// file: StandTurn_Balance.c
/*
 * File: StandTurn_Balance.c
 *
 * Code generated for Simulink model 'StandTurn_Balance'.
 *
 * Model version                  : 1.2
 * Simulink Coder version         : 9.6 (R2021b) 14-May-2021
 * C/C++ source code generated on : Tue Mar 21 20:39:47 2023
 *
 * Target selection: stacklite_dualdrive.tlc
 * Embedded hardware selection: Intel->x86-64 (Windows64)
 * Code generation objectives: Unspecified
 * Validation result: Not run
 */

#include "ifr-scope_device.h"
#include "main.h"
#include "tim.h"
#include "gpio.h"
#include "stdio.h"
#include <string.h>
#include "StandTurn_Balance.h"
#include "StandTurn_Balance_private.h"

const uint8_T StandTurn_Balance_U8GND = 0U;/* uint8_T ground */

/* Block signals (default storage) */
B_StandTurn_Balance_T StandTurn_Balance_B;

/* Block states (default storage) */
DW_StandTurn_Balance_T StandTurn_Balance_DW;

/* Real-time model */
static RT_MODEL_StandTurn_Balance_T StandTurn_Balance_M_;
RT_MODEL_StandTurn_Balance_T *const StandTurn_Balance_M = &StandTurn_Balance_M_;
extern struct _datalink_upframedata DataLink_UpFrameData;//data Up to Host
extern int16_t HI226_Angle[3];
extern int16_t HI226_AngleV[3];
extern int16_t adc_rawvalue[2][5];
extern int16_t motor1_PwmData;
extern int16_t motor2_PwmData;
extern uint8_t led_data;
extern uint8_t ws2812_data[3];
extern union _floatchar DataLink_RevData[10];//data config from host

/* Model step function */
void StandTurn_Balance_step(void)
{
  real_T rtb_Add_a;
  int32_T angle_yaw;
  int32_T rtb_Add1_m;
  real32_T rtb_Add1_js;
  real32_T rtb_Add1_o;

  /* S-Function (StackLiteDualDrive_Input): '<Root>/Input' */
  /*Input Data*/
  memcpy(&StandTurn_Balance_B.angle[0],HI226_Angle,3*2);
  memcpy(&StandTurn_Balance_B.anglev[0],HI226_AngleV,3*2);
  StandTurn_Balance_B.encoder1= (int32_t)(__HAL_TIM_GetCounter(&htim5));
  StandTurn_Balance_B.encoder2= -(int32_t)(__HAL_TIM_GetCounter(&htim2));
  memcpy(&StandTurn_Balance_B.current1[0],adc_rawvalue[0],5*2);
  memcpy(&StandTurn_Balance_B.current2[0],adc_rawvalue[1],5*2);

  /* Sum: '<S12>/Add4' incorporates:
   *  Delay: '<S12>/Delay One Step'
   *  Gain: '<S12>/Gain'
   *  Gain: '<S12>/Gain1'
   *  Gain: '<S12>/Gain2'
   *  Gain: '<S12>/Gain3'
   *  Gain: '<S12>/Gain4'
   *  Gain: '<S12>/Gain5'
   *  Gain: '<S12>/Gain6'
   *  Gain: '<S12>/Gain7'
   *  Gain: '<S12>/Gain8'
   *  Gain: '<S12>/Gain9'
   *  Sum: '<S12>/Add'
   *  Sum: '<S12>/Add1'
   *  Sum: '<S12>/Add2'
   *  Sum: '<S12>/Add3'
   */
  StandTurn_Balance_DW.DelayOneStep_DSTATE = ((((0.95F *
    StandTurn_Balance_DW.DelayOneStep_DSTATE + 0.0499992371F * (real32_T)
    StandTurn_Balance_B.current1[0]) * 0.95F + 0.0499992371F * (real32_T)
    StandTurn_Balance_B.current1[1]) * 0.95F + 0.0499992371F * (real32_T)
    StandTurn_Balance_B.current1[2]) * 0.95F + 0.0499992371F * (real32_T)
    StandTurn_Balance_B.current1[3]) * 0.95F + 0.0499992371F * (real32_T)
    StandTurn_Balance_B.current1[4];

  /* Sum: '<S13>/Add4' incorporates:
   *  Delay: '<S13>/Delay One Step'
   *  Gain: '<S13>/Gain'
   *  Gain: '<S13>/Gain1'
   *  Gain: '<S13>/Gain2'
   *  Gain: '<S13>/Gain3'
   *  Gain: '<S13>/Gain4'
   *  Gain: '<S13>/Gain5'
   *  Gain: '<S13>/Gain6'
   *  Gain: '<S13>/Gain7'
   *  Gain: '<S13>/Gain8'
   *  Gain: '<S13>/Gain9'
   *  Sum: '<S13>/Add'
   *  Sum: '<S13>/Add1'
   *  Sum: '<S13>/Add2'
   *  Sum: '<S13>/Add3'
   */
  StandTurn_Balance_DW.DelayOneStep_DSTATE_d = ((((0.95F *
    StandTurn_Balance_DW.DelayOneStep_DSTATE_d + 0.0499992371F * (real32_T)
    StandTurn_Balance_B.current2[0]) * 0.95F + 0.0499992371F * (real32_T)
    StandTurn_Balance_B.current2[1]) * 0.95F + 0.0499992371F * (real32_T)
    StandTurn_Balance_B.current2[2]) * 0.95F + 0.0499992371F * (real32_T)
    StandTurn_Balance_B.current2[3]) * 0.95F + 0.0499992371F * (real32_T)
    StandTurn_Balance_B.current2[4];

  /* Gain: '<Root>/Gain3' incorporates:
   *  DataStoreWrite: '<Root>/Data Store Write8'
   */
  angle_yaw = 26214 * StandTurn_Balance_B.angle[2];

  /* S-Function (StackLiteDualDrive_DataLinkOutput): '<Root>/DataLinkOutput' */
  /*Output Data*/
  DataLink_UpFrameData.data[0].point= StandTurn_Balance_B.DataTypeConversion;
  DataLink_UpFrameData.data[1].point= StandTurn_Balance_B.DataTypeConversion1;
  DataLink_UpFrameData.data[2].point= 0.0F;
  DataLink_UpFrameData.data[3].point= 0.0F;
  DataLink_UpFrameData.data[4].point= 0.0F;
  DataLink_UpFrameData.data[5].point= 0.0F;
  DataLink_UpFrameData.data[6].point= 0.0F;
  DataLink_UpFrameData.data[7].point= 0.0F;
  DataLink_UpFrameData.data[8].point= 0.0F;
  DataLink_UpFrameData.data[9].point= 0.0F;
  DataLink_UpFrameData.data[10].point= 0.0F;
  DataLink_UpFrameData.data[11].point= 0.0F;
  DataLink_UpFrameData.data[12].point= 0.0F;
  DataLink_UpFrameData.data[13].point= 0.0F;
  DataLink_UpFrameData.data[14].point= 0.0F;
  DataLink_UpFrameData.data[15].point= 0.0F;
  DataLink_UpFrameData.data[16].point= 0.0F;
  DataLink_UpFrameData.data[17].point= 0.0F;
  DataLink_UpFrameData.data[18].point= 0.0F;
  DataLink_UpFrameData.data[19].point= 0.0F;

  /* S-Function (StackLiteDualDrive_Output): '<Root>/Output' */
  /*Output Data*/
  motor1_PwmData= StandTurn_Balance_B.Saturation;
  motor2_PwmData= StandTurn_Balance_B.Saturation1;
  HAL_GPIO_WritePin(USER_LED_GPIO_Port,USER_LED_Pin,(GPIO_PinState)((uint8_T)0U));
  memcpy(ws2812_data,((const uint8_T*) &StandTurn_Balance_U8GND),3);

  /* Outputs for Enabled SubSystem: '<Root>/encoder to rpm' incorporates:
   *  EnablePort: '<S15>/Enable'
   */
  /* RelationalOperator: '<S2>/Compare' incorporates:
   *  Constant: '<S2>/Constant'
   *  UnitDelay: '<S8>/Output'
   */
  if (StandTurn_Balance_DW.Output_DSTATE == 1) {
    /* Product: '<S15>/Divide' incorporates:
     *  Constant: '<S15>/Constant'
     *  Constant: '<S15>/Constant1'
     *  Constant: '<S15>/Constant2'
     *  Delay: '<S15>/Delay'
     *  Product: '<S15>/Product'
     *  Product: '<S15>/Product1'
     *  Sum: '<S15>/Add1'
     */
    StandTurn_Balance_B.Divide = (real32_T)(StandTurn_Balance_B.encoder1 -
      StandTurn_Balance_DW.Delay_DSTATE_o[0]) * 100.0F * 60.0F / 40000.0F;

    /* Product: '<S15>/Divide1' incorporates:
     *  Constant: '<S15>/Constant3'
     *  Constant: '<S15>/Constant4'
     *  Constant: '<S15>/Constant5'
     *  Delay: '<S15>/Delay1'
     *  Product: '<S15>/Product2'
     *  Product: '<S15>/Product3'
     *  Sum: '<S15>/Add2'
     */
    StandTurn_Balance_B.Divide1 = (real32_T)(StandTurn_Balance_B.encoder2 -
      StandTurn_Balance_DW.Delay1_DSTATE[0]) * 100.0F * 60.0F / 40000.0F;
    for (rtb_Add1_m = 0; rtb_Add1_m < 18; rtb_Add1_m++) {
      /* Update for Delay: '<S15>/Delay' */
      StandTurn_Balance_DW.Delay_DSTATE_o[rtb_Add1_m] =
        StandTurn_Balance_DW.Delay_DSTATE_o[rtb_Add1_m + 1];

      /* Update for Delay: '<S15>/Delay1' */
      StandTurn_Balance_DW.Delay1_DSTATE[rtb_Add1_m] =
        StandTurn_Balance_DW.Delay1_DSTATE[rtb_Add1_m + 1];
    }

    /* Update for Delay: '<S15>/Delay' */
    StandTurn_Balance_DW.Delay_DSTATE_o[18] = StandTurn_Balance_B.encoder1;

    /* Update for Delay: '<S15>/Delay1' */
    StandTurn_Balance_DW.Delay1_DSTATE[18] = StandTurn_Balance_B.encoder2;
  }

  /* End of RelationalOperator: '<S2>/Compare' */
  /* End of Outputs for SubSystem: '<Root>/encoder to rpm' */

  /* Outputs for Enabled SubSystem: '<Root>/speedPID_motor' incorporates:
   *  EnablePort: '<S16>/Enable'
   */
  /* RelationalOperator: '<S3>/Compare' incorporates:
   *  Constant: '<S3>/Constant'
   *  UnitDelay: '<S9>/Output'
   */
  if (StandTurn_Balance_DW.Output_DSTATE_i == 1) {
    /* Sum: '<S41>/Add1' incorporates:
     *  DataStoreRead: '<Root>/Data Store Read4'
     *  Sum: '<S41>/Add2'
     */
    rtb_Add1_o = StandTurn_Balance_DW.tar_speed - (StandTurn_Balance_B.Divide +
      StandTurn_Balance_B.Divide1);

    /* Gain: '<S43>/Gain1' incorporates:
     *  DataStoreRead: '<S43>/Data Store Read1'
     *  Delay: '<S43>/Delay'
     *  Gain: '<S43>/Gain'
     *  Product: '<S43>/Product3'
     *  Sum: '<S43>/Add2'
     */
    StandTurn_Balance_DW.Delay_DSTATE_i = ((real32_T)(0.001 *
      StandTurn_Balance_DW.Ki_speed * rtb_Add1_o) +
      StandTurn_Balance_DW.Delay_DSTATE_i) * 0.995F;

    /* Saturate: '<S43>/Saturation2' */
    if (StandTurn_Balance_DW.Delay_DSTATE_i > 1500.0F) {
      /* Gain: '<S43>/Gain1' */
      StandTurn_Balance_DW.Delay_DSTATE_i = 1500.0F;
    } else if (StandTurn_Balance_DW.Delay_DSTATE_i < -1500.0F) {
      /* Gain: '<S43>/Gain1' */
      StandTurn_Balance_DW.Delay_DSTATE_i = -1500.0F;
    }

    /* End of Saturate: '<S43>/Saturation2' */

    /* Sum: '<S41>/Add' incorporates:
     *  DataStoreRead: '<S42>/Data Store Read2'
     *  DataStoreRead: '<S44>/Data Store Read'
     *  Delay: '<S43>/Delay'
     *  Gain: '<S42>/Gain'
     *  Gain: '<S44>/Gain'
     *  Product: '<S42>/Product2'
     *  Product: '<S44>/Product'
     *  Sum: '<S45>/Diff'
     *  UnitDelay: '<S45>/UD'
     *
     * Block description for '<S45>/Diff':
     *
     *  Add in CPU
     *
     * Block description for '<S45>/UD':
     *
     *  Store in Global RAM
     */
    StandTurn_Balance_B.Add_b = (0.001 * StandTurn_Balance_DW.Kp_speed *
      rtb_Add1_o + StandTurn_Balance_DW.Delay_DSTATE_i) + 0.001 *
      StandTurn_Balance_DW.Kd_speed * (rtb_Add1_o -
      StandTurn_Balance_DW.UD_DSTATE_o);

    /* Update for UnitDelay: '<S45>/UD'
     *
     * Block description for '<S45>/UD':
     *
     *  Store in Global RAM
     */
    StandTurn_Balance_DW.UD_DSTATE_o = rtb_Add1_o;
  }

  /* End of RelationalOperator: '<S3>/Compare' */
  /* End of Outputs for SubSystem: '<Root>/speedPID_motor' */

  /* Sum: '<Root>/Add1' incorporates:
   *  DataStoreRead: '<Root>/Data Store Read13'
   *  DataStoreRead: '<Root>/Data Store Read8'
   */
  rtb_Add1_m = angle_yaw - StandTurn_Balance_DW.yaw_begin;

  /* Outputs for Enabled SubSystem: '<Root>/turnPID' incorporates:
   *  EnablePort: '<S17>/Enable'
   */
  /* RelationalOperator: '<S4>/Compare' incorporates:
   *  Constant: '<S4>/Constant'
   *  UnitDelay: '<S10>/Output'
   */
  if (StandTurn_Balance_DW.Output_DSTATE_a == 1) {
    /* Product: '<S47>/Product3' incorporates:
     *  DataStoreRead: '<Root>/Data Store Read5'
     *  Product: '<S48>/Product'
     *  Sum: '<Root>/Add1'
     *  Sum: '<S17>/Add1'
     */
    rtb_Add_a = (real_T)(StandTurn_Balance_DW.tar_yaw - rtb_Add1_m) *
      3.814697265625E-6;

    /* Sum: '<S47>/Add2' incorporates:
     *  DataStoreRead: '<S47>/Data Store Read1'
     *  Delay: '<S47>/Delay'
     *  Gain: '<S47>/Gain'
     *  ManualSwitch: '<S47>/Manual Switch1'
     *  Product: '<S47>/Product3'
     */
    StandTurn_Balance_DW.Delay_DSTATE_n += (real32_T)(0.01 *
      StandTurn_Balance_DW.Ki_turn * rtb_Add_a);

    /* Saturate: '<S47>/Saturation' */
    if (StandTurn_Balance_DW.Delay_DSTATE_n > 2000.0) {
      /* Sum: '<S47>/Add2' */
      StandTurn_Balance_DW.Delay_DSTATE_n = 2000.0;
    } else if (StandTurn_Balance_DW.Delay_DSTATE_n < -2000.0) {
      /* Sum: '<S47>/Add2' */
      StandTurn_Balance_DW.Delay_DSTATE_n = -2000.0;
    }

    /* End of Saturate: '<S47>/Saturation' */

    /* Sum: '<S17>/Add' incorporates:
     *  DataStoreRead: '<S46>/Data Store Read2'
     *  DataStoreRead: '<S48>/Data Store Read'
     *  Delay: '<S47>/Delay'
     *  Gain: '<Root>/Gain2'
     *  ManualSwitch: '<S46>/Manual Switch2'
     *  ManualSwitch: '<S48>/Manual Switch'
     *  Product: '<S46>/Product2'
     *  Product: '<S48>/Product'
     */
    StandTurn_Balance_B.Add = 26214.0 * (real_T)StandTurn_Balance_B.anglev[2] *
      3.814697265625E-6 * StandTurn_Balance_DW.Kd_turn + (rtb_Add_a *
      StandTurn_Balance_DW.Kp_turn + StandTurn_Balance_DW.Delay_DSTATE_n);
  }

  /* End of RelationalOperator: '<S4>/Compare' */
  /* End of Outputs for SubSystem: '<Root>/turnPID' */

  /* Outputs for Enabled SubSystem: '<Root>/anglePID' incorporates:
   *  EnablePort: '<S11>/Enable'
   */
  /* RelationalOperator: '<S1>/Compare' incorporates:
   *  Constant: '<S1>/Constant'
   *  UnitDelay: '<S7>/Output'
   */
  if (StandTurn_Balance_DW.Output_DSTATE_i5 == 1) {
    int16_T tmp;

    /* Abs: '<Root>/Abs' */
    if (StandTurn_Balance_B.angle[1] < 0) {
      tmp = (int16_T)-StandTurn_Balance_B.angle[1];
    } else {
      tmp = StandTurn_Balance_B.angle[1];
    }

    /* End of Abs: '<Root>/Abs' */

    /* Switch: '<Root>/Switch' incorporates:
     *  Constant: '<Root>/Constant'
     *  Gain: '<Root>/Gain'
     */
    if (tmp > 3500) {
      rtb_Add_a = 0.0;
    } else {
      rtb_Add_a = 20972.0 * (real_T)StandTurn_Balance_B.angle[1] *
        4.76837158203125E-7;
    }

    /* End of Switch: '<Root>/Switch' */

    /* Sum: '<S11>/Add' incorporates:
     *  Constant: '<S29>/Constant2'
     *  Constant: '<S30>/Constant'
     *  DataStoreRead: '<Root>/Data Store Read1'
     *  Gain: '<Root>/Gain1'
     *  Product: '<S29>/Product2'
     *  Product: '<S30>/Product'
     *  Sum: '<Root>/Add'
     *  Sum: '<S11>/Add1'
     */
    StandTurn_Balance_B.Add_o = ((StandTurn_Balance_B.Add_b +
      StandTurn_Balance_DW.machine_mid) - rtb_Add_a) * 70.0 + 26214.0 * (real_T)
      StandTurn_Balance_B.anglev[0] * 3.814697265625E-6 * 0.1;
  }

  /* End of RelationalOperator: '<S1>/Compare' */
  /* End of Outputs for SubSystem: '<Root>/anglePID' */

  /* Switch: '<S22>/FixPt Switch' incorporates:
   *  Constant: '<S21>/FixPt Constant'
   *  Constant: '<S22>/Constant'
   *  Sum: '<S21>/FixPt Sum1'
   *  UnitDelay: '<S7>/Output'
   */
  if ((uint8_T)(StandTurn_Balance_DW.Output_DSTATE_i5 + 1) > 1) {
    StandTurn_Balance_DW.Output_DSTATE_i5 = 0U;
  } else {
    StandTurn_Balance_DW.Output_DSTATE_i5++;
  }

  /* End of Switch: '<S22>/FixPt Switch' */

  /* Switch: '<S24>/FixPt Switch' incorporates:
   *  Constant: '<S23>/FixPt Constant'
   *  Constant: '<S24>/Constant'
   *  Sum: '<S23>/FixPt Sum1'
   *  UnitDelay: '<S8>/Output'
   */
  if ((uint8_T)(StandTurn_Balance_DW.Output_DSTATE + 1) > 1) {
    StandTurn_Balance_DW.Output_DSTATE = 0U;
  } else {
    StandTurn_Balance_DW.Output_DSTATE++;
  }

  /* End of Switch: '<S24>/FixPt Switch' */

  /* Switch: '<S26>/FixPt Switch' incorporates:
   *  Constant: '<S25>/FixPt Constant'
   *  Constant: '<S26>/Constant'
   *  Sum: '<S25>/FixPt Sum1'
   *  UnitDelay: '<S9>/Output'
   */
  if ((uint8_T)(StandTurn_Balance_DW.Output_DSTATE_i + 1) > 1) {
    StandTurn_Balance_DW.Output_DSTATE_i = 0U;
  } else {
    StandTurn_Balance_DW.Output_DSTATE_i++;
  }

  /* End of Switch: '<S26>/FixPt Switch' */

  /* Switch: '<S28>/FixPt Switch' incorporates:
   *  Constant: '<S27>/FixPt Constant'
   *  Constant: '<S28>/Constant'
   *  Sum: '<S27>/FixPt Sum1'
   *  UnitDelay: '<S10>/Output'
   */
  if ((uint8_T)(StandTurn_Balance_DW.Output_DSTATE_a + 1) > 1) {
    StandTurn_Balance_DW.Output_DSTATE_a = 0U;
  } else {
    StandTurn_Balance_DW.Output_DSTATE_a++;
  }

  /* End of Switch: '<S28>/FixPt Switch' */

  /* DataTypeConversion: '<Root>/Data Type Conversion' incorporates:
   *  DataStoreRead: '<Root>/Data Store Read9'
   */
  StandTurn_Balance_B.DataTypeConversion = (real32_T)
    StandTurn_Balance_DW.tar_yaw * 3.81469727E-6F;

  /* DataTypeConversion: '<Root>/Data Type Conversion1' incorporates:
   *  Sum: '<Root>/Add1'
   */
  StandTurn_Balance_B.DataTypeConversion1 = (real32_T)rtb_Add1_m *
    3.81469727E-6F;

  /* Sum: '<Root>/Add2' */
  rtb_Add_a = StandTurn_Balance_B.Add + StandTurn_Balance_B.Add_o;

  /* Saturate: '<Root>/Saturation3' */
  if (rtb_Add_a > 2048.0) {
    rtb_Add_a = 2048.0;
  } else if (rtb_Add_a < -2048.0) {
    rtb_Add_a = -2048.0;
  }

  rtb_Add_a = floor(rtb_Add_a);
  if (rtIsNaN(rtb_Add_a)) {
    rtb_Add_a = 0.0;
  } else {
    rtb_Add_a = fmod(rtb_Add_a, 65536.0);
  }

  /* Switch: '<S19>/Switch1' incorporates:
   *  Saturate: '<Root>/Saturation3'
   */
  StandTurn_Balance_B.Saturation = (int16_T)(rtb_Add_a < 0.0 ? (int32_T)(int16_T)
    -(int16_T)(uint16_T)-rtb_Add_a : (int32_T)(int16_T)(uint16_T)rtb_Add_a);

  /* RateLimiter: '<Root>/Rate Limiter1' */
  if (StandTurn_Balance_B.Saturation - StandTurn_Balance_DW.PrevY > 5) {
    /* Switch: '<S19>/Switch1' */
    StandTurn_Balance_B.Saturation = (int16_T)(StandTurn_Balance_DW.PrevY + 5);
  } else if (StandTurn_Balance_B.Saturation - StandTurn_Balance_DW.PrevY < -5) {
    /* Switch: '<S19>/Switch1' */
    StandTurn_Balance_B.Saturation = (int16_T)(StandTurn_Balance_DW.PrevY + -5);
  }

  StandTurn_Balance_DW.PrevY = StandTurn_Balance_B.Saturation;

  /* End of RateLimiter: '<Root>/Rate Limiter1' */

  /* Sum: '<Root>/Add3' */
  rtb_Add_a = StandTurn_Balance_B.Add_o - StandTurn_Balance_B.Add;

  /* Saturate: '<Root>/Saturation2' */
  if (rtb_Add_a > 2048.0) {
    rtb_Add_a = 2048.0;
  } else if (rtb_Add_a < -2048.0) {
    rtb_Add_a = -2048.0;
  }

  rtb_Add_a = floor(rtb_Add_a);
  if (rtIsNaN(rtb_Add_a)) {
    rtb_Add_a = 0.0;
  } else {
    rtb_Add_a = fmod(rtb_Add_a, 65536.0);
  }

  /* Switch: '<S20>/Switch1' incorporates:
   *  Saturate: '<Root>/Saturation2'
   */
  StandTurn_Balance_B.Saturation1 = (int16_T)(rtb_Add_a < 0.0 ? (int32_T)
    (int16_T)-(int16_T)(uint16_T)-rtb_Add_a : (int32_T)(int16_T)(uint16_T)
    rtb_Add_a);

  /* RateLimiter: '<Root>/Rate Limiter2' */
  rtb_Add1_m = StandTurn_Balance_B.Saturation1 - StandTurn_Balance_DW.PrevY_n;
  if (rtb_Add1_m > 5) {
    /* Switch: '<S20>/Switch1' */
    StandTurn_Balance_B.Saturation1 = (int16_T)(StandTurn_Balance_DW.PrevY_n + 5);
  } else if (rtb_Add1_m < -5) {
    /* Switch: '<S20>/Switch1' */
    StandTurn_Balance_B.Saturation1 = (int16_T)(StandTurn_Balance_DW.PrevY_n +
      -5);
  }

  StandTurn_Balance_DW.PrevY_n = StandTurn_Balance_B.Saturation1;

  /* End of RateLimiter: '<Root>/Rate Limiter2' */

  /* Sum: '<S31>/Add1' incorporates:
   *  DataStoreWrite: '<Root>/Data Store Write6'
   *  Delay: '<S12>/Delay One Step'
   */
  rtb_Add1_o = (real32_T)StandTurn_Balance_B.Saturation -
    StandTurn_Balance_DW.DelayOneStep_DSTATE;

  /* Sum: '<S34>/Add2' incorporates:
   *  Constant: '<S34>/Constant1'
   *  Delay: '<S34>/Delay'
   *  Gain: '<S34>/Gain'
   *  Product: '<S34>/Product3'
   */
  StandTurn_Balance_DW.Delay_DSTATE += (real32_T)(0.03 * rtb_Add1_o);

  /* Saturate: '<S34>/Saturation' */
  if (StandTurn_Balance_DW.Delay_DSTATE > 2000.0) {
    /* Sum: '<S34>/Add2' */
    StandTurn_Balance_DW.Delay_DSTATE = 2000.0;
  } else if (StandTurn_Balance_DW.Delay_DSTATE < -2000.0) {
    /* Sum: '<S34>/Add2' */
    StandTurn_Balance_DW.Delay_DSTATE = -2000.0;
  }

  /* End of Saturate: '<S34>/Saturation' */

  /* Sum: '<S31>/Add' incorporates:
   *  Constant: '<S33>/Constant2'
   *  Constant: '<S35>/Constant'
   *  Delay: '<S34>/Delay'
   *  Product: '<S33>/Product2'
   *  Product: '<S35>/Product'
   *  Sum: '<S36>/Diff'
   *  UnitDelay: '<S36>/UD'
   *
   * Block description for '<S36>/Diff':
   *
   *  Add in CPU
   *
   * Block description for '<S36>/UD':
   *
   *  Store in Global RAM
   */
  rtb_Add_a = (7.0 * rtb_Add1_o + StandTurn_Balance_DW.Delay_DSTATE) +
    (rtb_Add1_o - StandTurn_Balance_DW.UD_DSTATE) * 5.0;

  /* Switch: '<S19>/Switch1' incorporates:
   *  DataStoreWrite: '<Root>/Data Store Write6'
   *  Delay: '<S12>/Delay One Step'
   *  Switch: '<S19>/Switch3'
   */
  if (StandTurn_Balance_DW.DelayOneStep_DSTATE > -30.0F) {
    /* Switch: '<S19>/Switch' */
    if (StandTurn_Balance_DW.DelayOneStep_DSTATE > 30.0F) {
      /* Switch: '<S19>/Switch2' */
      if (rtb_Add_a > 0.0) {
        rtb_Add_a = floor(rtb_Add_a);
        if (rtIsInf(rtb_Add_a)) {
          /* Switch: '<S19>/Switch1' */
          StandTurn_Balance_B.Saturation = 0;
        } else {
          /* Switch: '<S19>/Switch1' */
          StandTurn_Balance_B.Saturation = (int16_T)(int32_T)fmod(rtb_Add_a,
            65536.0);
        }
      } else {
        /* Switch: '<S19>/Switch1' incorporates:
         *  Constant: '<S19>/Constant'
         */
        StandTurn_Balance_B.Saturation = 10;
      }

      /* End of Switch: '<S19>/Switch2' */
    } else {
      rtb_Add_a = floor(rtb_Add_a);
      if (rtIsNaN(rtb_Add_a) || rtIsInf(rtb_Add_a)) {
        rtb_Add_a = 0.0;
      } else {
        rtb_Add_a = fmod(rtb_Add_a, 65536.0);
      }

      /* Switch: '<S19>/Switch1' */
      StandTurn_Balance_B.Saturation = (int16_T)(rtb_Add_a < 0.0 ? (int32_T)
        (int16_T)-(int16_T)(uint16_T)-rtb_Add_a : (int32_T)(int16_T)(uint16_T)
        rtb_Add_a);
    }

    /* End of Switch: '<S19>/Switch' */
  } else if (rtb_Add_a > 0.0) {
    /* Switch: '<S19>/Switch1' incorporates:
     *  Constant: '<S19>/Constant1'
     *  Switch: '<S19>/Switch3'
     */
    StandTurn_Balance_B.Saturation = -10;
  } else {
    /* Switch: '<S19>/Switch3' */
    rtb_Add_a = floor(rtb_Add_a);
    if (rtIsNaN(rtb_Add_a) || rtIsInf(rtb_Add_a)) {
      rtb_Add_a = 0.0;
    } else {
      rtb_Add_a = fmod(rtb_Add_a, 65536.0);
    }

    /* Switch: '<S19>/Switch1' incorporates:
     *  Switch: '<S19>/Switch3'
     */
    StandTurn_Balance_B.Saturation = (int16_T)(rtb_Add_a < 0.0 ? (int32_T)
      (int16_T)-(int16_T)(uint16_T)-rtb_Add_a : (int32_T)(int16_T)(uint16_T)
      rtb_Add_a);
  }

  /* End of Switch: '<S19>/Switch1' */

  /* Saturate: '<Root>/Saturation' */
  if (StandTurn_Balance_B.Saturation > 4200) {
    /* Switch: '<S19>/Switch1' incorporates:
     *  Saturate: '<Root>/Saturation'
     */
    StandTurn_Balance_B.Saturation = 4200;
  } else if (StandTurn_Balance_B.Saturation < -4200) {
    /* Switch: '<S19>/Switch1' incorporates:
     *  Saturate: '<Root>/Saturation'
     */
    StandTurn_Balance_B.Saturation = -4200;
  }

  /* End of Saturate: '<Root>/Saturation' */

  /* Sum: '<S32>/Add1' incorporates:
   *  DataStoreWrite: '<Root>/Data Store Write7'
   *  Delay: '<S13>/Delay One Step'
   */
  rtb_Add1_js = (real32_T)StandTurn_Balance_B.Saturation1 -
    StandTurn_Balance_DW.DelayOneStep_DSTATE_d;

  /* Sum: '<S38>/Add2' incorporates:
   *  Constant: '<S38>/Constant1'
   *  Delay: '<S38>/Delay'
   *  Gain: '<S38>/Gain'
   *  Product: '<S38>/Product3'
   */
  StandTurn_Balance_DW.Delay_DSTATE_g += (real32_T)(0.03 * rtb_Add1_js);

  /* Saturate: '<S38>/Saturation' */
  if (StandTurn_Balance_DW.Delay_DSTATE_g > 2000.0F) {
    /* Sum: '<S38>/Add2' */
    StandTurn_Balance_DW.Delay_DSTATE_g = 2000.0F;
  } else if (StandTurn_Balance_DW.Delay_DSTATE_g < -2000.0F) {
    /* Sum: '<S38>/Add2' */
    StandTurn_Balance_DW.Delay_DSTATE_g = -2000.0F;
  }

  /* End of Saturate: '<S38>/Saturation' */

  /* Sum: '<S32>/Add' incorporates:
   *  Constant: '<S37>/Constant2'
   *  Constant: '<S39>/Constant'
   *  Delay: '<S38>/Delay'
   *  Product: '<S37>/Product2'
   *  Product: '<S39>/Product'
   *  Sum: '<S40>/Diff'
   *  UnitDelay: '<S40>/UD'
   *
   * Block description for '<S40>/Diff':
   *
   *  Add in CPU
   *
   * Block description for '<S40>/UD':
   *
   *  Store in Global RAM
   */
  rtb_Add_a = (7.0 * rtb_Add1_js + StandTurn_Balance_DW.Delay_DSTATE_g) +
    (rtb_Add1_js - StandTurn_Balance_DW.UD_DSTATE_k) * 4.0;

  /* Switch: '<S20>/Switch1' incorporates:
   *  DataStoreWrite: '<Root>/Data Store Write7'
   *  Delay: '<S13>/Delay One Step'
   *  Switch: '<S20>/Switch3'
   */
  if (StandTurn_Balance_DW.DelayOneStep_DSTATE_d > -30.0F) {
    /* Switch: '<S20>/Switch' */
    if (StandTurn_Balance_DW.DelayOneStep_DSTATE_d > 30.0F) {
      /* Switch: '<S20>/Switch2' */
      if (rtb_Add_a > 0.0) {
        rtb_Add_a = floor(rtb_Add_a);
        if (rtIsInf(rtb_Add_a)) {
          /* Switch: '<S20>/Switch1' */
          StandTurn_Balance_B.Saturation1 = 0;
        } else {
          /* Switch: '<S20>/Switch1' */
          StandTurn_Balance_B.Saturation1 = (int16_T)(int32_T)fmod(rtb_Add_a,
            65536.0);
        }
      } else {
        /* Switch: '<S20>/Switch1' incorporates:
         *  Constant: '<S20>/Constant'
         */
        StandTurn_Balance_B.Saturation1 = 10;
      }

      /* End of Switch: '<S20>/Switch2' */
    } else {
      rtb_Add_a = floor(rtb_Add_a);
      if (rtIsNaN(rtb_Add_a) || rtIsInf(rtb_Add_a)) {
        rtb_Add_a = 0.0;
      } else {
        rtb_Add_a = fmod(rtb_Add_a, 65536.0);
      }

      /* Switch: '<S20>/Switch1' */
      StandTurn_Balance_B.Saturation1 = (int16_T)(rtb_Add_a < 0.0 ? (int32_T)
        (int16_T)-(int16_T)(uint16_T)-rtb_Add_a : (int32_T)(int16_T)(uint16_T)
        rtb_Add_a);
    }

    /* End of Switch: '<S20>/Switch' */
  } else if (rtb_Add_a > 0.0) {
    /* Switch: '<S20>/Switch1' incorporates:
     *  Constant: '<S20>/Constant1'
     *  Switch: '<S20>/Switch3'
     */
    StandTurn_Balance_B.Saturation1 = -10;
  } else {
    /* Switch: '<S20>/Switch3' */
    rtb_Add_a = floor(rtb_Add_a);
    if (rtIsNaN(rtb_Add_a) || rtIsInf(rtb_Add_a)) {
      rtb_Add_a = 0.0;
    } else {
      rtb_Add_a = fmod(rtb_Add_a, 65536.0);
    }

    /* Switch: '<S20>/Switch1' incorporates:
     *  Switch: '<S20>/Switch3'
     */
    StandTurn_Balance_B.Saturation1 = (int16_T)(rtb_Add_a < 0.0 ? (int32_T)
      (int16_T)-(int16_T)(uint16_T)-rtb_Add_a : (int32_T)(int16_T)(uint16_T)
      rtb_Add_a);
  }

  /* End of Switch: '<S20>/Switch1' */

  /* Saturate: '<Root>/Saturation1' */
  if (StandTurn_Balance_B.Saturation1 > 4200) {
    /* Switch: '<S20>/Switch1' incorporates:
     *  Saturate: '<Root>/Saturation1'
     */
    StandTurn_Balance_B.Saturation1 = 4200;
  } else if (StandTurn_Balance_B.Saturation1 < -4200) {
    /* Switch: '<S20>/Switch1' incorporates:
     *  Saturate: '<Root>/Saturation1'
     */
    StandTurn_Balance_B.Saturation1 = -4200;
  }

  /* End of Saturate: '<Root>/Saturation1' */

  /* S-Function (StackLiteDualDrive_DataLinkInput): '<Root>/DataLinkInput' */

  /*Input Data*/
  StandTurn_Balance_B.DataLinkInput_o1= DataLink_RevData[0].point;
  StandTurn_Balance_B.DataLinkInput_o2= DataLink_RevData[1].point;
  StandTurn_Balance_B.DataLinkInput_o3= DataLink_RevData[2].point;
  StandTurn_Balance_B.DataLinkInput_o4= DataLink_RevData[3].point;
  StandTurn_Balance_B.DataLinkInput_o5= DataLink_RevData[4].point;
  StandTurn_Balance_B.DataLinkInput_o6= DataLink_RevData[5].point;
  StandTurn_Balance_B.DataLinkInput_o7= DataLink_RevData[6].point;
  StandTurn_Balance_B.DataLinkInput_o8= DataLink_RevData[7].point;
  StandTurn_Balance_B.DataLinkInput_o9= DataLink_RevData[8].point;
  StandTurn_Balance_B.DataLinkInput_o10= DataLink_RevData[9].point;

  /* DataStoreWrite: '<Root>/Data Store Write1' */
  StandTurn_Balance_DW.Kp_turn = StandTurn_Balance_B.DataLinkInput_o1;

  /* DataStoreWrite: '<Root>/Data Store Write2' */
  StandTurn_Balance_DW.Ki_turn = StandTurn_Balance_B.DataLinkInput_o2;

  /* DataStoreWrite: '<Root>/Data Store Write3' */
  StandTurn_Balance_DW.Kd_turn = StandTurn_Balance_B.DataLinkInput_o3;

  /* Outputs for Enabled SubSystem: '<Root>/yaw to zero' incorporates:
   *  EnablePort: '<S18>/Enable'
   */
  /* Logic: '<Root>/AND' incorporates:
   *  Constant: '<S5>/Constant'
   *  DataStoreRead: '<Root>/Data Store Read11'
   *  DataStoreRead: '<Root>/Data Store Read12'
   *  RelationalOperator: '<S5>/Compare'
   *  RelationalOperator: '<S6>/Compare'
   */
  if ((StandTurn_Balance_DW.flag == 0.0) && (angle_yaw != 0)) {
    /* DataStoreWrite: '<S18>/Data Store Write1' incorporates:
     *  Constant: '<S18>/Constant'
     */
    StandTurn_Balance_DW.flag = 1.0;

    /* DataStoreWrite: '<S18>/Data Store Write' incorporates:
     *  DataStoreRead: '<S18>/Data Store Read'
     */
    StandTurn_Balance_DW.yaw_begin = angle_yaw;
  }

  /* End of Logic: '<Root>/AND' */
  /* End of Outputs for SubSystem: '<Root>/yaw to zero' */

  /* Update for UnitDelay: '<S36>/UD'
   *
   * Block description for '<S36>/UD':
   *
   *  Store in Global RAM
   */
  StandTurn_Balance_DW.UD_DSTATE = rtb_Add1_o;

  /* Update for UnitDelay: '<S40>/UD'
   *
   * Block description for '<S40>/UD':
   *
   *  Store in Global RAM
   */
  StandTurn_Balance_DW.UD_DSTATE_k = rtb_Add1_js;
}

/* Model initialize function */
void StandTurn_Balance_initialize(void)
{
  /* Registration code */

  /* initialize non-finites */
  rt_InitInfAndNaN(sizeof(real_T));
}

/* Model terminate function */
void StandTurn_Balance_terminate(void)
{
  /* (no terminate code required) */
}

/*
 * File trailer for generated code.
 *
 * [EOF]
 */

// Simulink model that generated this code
simulink model "StandTurn_Balance"  (R2021b)
settings: Solver=FixedStepDiscrete  StartTime=0.0  StopTime=inf  FixedStep=0.0005  RelTol=1e-3
libraries: simulink x13, IFR_StackLiteDualDrive_SimulinkLib x4

== system StandTurn_Balance ==
  AND : Logic  IconShape=distinctive  AllPortsSameDT=off  OutDataTypeStr=boolean
  Abs : Abs
  Add : Sum
  Add1 : Sum  Inputs=+-
  Add2 : Sum
  Add3 : Sum  Inputs=-+
  Compare To Constant{,1..3} (4 alike) : simulink/Logic and Bit Operations/Compare To Constant  relop===  const=1  OutDataTypeStr=boolean
  Compare To Constant4 : simulink/Logic and Bit Operations/Compare To Constant  relop===  const=0  OutDataTypeStr=boolean
  Compare To Constant5 : simulink/Logic and Bit Operations/Compare To Constant  relop=~=  const=0  OutDataTypeStr=boolean
  Constant : Constant  Value=0
  Counter Limited{,1..3} (4 alike) : simulink/Sources/Counter Limited  uplimit=1  tsamp=-1
  Data Store Memory : DataStoreMemory  DataStoreName=Kp_angle  ReadBeforeWriteMsg=warning  WriteAfterWriteMsg=warning  WriteAfterReadMsg=warning  ShowAdditionalParam=off
  Data Store Memory1 : DataStoreMemory  DataStoreName=angleV_pitch  ReadBeforeWriteMsg=warning  WriteAfterWriteMsg=warning  WriteAfterReadMsg=warning  ShowAdditionalParam=off
  Data Store Memory10 : DataStoreMemory  DataStoreName=flag  ReadBeforeWriteMsg=warning  WriteAfterWriteMsg=warning  WriteAfterReadMsg=warning  ShowAdditionalParam=off
  Data Store Memory11 : DataStoreMemory  DataStoreName=yaw_begin  ReadBeforeWriteMsg=warning  WriteAfterWriteMsg=warning  WriteAfterReadMsg=warning  ShowAdditionalParam=off
  Data Store Memory12 : DataStoreMemory  DataStoreName=tar_speed  ReadBeforeWriteMsg=warning  WriteAfterWriteMsg=warning  WriteAfterReadMsg=warning  ShowAdditionalParam=off
  Data Store Memory13 : DataStoreMemory  DataStoreName=Kp_speed  ReadBeforeWriteMsg=warning  WriteAfterWriteMsg=warning  WriteAfterReadMsg=warning  ShowAdditionalParam=off
  Data Store Memory14 : DataStoreMemory  DataStoreName=Ki_speed  ReadBeforeWriteMsg=warning  WriteAfterWriteMsg=warning  WriteAfterReadMsg=warning  ShowAdditionalParam=off
  Data Store Memory15 : DataStoreMemory  DataStoreName=Kd_speed  ReadBeforeWriteMsg=warning  WriteAfterWriteMsg=warning  WriteAfterReadMsg=warning  ShowAdditionalParam=off
  Data Store Memory16 : DataStoreMemory  DataStoreName=angleV_yaw  ReadBeforeWriteMsg=warning  WriteAfterWriteMsg=warning  WriteAfterReadMsg=warning  ShowAdditionalParam=off
  Data Store Memory19 : DataStoreMemory  DataStoreName=Kp_turn  ReadBeforeWriteMsg=warning  WriteAfterWriteMsg=warning  WriteAfterReadMsg=warning  ShowAdditionalParam=off
  Data Store Memory2 : DataStoreMemory  DataStoreName=Kd_angle  ReadBeforeWriteMsg=warning  WriteAfterWriteMsg=warning  WriteAfterReadMsg=warning  ShowAdditionalParam=off
  Data Store Memory20 : DataStoreMemory  DataStoreName=tar_yaw  ReadBeforeWriteMsg=warning  WriteAfterWriteMsg=warning  WriteAfterReadMsg=warning  ShowAdditionalParam=off
  Data Store Memory21 : DataStoreMemory  DataStoreName=angle_yaw  ReadBeforeWriteMsg=warning  WriteAfterWriteMsg=warning  WriteAfterReadMsg=warning  ShowAdditionalParam=off
  Data Store Memory22 : DataStoreMemory  DataStoreName=Ki_turn  ReadBeforeWriteMsg=warning  WriteAfterWriteMsg=warning  WriteAfterReadMsg=warning  ShowAdditionalParam=off
  Data Store Memory23 : DataStoreMemory  DataStoreName=Kd_turn  ReadBeforeWriteMsg=warning  WriteAfterWriteMsg=warning  WriteAfterReadMsg=warning  ShowAdditionalParam=off
  Data Store Memory3 : DataStoreMemory  DataStoreName=Kp_current  ReadBeforeWriteMsg=warning  WriteAfterWriteMsg=warning  WriteAfterReadMsg=warning  ShowAdditionalParam=off
  Data Store Memory4 : DataStoreMemory  DataStoreName=Ki_current  ReadBeforeWriteMsg=warning  WriteAfterWriteMsg=warning  WriteAfterReadMsg=warning  ShowAdditionalParam=off
  Data Store Memory5 : DataStoreMemory  DataStoreName=Kd_current  ReadBeforeWriteMsg=warning  WriteAfterWriteMsg=warning  WriteAfterReadMsg=warning  ShowAdditionalParam=off
  Data Store Memory6 : DataStoreMemory  DataStoreName=tar_current  ReadBeforeWriteMsg=warning  WriteAfterWriteMsg=warning  WriteAfterReadMsg=warning  ShowAdditionalParam=off
  Data Store Memory7 : DataStoreMemory  DataStoreName=machine_mid  ReadBeforeWriteMsg=warning  WriteAfterWriteMsg=warning  WriteAfterReadMsg=warning  ShowAdditionalParam=off
  Data Store Memory8 : DataStoreMemory  DataStoreName=now_current1  ReadBeforeWriteMsg=warning  WriteAfterWriteMsg=warning  WriteAfterReadMsg=warning  ShowAdditionalParam=off
  Data Store Memory9 : DataStoreMemory  DataStoreName=now_current2  ReadBeforeWriteMsg=warning  WriteAfterWriteMsg=warning  WriteAfterReadMsg=warning  ShowAdditionalParam=off
  Data Store Read : DataStoreRead  DataStoreName=tar_current  IndexOptions=Index vector (dialog)  Indices=1  OutputSizes=1
  Data Store Read1 : DataStoreRead  DataStoreName=machine_mid  IndexOptions=Index vector (dialog)  Indices=1  OutputSizes=1
  Data Store Read11 : DataStoreRead  DataStoreName=flag  IndexOptions=Index vector (dialog)  Indices=1  OutputSizes=1
  Data Store Read12 : DataStoreRead  DataStoreName=angle_yaw  IndexOptions=Index vector (dialog)  Indices=1  OutputSizes=1
  Data Store Read13 : DataStoreRead  DataStoreName=yaw_begin  IndexOptions=Index vector (dialog)  Indices=1  OutputSizes=1
  Data Store Read2 : DataStoreRead  DataStoreName=now_current1  IndexOptions=Index vector (dialog)  Indices=1  OutputSizes=1
  Data Store Read3 : DataStoreRead  DataStoreName=now_current2  IndexOptions=Index vector (dialog)  Indices=1  OutputSizes=1
  Data Store Read4 : DataStoreRead  DataStoreName=tar_speed  IndexOptions=Index vector (dialog)  Indices=1  OutputSizes=1
  Data Store Read5 : DataStoreRead  DataStoreName=tar_yaw  IndexOptions=Index vector (dialog)  Indices=1  OutputSizes=1
  Data Store Read6 : DataStoreRead  DataStoreName=now_current1  IndexOptions=Index vector (dialog)  Indices=1  OutputSizes=1
  Data Store Read7 : DataStoreRead  DataStoreName=now_current2  IndexOptions=Index vector (dialog)  Indices=1  OutputSizes=1
  Data Store Read8 : DataStoreRead  DataStoreName=angle_yaw  IndexOptions=Index vector (dialog)  Indices=1  OutputSizes=1
  Data Store Read9 : DataStoreRead  DataStoreName=tar_yaw  IndexOptions=Index vector (dialog)  Indices=1  OutputSizes=1
  Data Store Write : DataStoreWrite  DataStoreName=angleV_pitch  IndexOptions=Index vector (dialog)  Indices=1  OutputSizes=1
  Data Store Write1 : DataStoreWrite  DataStoreName=Kp_turn  IndexOptions=Index vector (dialog)  Indices=1  OutputSizes=1
  Data Store Write2 : DataStoreWrite  DataStoreName=Ki_turn  IndexOptions=Index vector (dialog)  Indices=1  OutputSizes=1
  Data Store Write3 : DataStoreWrite  DataStoreName=Kd_turn  IndexOptions=Index vector (dialog)  Indices=1  OutputSizes=1
  Data Store Write6 : DataStoreWrite  DataStoreName=now_current1  IndexOptions=Index vector (dialog)  Indices=1  OutputSizes=1
  Data Store Write7 : DataStoreWrite  DataStoreName=now_current2  IndexOptions=Index vector (dialog)  Indices=1  OutputSizes=1
  Data Store Write8 : DataStoreWrite  DataStoreName=angle_yaw  IndexOptions=Index vector (dialog)  Indices=1  OutputSizes=1
  Data Store Write9 : DataStoreWrite  DataStoreName=angleV_yaw  IndexOptions=Index vector (dialog)  Indices=1  OutputSizes=1
  Data Type Conversion : DataTypeConversion  OutDataTypeStr=single
  Data Type Conversion1 : DataTypeConversion  OutDataTypeStr=single
  DataLinkInput : IFR_StackLiteDualDrive_SimulinkLib/DataLinkInput
  DataLinkOutput : IFR_StackLiteDualDrive_SimulinkLib/DataLinkOutput  id='BalanceUnname'  key='IFR00'
  Demux : Demux  Outputs=3
  Demux1 : Demux  Outputs=5
  Demux2 : Demux  Outputs=5
  Demux3 : Demux  Outputs=3
  Gain : Gain  Gain=0.01
  Gain1 : Gain  Gain=0.1
  Gain2 : Gain  Gain=0.1
  Gain3 : Gain  Gain=0.1
  Input : IFR_StackLiteDualDrive_SimulinkLib/Input  Priority=0
  Manual Switch : ManualSwitch  CurrentSetting=0
  Output : IFR_StackLiteDualDrive_SimulinkLib/Output  Priority=255
  Rate Limiter1 : RateLimiter  RisingSlewLimit=10000  FallingSlewLimit=-10000  SampleTimeMode=inherited
  Rate Limiter2 : RateLimiter  RisingSlewLimit=10000  FallingSlewLimit=-10000  SampleTimeMode=inherited
  Saturation : Saturate  UpperLimit=4200  LowerLimit=-4200
  Saturation1 : Saturate  UpperLimit=4200  LowerLimit=-4200
  Saturation2 : Saturate  UpperLimit=2048  LowerLimit=-2048  OutDataTypeStr=int16
  Saturation3 : Saturate  UpperLimit=2048  LowerLimit=-2048  OutDataTypeStr=int16
  Switch : Switch  Criteria=u2 > Threshold  Threshold=3500
  Terminator{,1..8} (9 alike) : Terminator
  anglePID : Subsystem
  currentFilter_motor1 : Subsystem
  currentFilter_motor2 : Subsystem
  currentPID : Subsystem
  encoder to rpm : Subsystem
  speedPID_motor : Subsystem
  turnPID : Subsystem
  yaw to zero : Subsystem
  zero limit1 : Subsystem
  zero limit2 : Subsystem
  wires:
  Input/5 -> Demux2/1  "current1"
  Saturation1/1 -> Output/2
  Saturation2/1 -> Rate Limiter2/1
  Data Store Read3/1 -> currentPID/3(now_current2)
  Rate Limiter2/1 -> currentPID/4(tar_current2)
  Input/1 -> Demux/1  "angle"
  currentFilter_motor2/1(now_current) -> Data Store Write7/1
  Manual Switch/1 -> currentPID/1(tar_current1)
  Compare To Constant1/1 -> encoder to rpm/Enable
  Demux1/4 -> currentFilter_motor2/4(In4)
  Counter Limited1/1 -> Compare To Constant1/1
  Demux2/2 -> currentFilter_motor1/2(In2)
  zero limit2/1(pwmout) -> Saturation1/1  "motor2pwm"
  Demux1/1 -> currentFilter_motor2/1(In1)
  Demux2/5 -> currentFilter_motor1/5(In5)
  Input/3 -> encoder to rpm/1(encoder1)  "encoder1"
  Saturation3/1 -> Rate Limiter1/1
  Saturation/1 -> Output/1
  Demux1/3 -> currentFilter_motor2/3(In3)
  Input/6 -> Demux1/1  "current2"
  Demux2/3 -> currentFilter_motor1/3(In3)
  Demux/3 -> Gain3/1
  currentPID/2(tar_V2) -> zero limit2/1(pidout2pwm)
  Input/2 -> Demux3/1  "anglev"
  Demux3/2 -> Terminator6/1
  Demux2/1 -> currentFilter_motor1/1(In1)
  Demux1/5 -> currentFilter_motor2/5(In5)
  Input/4 -> encoder to rpm/2(encoder2)  "encoder2"
  currentPID/1(tar_V1) -> zero limit1/1(pidout1pwm)
  Demux1/2 -> currentFilter_motor2/2(In2)
  Data Store Read2/1 -> currentPID/2(now_current1)
  Data Store Read7/1 -> zero limit2/2(current2)
  currentFilter_motor1/1(now_current) -> Data Store Write6/1
  Rate Limiter1/1 -> Manual Switch/2
  Demux2/4 -> currentFilter_motor1/4(In4)
  zero limit1/1(pwmout) -> Saturation/1  "motor1pwm"
  Data Store Read/1 -> Manual Switch/1
  Data Store Read6/1 -> zero limit1/2(current1)
  Add/1 -> anglePID/1(tar_angle)
  Abs/1 -> Switch/2
  Gain/1 -> Switch/3
  Constant/1 -> Switch/1
  Demux/2 -> Gain/1, Abs/1
  Counter Limited/1 -> Compare To Constant/1
  Switch/1 -> anglePID/2(now_angle)
  Data Store Read1/1 -> Add/2
  Compare To Constant/1 -> anglePID/Enable
  Demux/1 -> Terminator7/1
  speedPID_motor/1(tar_sqangle) -> Add/1
  Demux3/1 -> Gain1/1
  Gain1/1 -> Data Store Write/1
  Data Store Read4/1 -> speedPID_motor/1(tar_speed)
  Counter Limited2/1 -> Compare To Constant2/1
  Compare To Constant2/1 -> speedPID_motor/Enable
  encoder to rpm/1(now_speed1) -> speedPID_motor/2(now_speed1)
  encoder to rpm/2(now_speed2) -> speedPID_motor/3(now_speed2)
  Data Store Read5/1 -> turnPID/1(tar_yaw)
  Demux3/3 -> Gain2/1
  Gain2/1 -> Data Store Write9/1
  Gain3/1 -> Data Store Write8/1
  turnPID/1(tar_I) -> Add3/1, Add2/1
  anglePID/1(tar_I) -> Add2/2, Add3/2
  Add2/1 -> Saturation3/1
  Add3/1 -> Saturation2/1
  Compare To Constant3/1 -> turnPID/Enable
  Counter Limited3/1 -> Compare To Constant3/1
  Data Store Read9/1 -> Data Type Conversion/1
  Data Type Conversion/1 -> DataLinkOutput/1
  Add1/1 -> Data Type Conversion1/1, turnPID/2(now_yaw)
  Data Type Conversion1/1 -> DataLinkOutput/2
  Data Store Read11/1 -> Compare To Constant4/1
  Data Store Read12/1 -> Compare To Constant5/1
  Compare To Constant4/1 -> AND/1
  Compare To Constant5/1 -> AND/2
  AND/1 -> yaw to zero/Enable
  Data Store Read8/1 -> Add1/1
  Data Store Read13/1 -> Add1/2
  DataLinkInput/10 -> Terminator/1
  DataLinkInput/9 -> Terminator1/1
  DataLinkInput/8 -> Terminator2/1
  DataLinkInput/7 -> Terminator3/1
  DataLinkInput/6 -> Terminator4/1
  DataLinkInput/5 -> Terminator5/1
  DataLinkInput/4 -> Terminator8/1
  DataLinkInput/1 -> Data Store Write1/1
  DataLinkInput/2 -> Data Store Write2/1
  DataLinkInput/3 -> Data Store Write3/1

== system StandTurn_Balance/anglePID ==
  tar_angle : Inport
  now_angle : Inport  Port=2
  Enable : EnablePort
  Add : Sum  OutDataTypeStr=double
  Add1 : Sum  Inputs=+-
  D : Subsystem
  P : Subsystem
  tar_I : Outport
  wires:
  Add/1 -> tar_I/1
  D/1(Out1) -> Add/2
  now_angle/1 -> Add1/2
  tar_angle/1 -> Add1/1
  P/1(Out1) -> Add/1
  Add1/1 -> P/1(error)

== system StandTurn_Balance/currentFilter_motor1 ==
  In1 : Inport
  In2 : Inport  Port=2
  In3 : Inport  Port=3
  In4 : Inport  Port=4
  In5 : Inport  Port=5
  Add{,1..4} (5 alike) : Sum
  Delay One Step : Delay  DelayLength=1
  Gain{,2,4,6,8} (5 alike) : Gain  Gain=0.05  OutDataTypeStr=single
  Gain{1,3,5,7,9} (5 alike) : Gain  Gain=0.95  OutDataTypeStr=single
  now_current : Outport
  wires:
  Gain1/1 -> Add/1
  Gain5/1 -> Add2/1
  Gain/1 -> Add/2
  Gain3/1 -> Add1/1
  In2/1 -> Gain2/1
  Gain2/1 -> Add1/2
  Delay One Step/1 -> Gain1/1
  In1/1 -> Gain/1
  Add/1 -> Gain3/1
  Gain4/1 -> Add2/2
  In4/1 -> Gain6/1
  Add1/1 -> Gain5/1
  Gain9/1 -> Add4/1
  Add2/1 -> Gain7/1
  Gain8/1 -> Add4/2
  Gain7/1 -> Add3/1
  Add4/1 -> now_current/1, Delay One Step/1
  Gain6/1 -> Add3/2
  Add3/1 -> Gain9/1
  In5/1 -> Gain8/1
  In3/1 -> Gain4/1

== system StandTurn_Balance/currentFilter_motor2 ==
  In1 : Inport
  In2 : Inport  Port=2
  In3 : Inport  Port=3
  In4 : Inport  Port=4
  In5 : Inport  Port=5
  Add{,1..4} (5 alike) : Sum
  Delay One Step : Delay  DelayLength=1
  Gain{,2,4,6,8} (5 alike) : Gain  Gain=0.05  OutDataTypeStr=single
  Gain{1,3,5,7,9} (5 alike) : Gain  Gain=0.95  OutDataTypeStr=single
  now_current : Outport
  wires:
  In3/1 -> Gain4/1
  In5/1 -> Gain8/1
  Add3/1 -> Gain9/1
  Gain6/1 -> Add3/2
  Add4/1 -> Delay One Step/1, now_current/1
  Gain7/1 -> Add3/1
  Gain8/1 -> Add4/2
  Add2/1 -> Gain7/1
  Gain9/1 -> Add4/1
  Add1/1 -> Gain5/1
  In4/1 -> Gain6/1
  Gain4/1 -> Add2/2
  Add/1 -> Gain3/1
  In1/1 -> Gain/1
  Delay One Step/1 -> Gain1/1
  Gain2/1 -> Add1/2
  In2/1 -> Gain2/1
  Gain3/1 -> Add1/1
  Gain/1 -> Add/2
  Gain5/1 -> Add2/1
  Gain1/1 -> Add/1

== system StandTurn_Balance/currentPID ==
  tar_current1 : Inport
  now_current1 : Inport  Port=2
  now_current2 : Inport  Port=3
  tar_current2 : Inport  Port=4
  currentPID_motor1 : Subsystem
  currentPID_motor2 : Subsystem
  tar_V1 : Outport
  tar_V2 : Outport  Port=2
  wires:
  tar_current1/1 -> currentPID_motor1/1(tar_current)
  now_current1/1 -> currentPID_motor1/2(now_current)
  currentPID_motor1/1(tar_V) -> tar_V1/1
  now_current2/1 -> currentPID_motor2/2(now_current)
  currentPID_motor2/1(tar_V) -> tar_V2/1
  tar_current2/1 -> currentPID_motor2/1(tar_current)

== system StandTurn_Balance/encoder to rpm ==
  note: 将读到的编码器值转化为电机转速rpm
      | 电机转一圈编码器输出值为40000
      | simulink最外层运行频率为2kHz，
      | 使用延时模块，每次输出1/ 2k*20=10ms编码器增加的值
  encoder1 : Inport
  encoder2 : Inport  Port=2
  Enable : EnablePort
  Add1 : Sum  Inputs=+-
  Add2 : Sum  Inputs=+-
  Constant : Constant  Value=40000  OutDataTypeStr=single
  Constant1 : Constant  Value=100  OutDataTypeStr=single
  Constant2 : Constant  Value=60  OutDataTypeStr=single
  Constant3 : Constant  Value=40000  OutDataTypeStr=single
  Constant4 : Constant  Value=100  OutDataTypeStr=single
  Constant5 : Constant  Value=60  OutDataTypeStr=single
  Delay : Delay  DelayLength=19
  Delay1 : Delay  DelayLength=19
  Divide : Product  Inputs=*/  OutDataTypeStr=single
  Divide1 : Product  Inputs=*/  OutDataTypeStr=single
  Product{,1..3} (4 alike) : Product  OutDataTypeStr=single
  now_speed1 : Outport
  now_speed2 : Outport  Port=2
  wires:
  Product1/1 -> Divide/1
  Product/1 -> Product1/1
  Constant/1 -> Divide/2
  encoder1/1 -> Add1/1, Delay/1
  Add2/1 -> Product2/1
  Delay1/1 -> Add2/2
  encoder2/1 -> Add2/1, Delay1/1
  Constant1/1 -> Product/2
  Add1/1 -> Product/1
  Constant2/1 -> Product1/2
  Delay/1 -> Add1/2
  Divide1/1 -> now_speed2/1
  Product2/1 -> Product3/1
  Constant4/1 -> Product2/2
  Product3/1 -> Divide1/1
  Constant5/1 -> Product3/2
  Divide/1 -> now_speed1/1
  Constant3/1 -> Divide1/2

== system StandTurn_Balance/speedPID_motor ==
  tar_speed : Inport
  now_speed1 : Inport  Port=2
  now_speed2 : Inport  Port=3
  Enable : EnablePort
  Subsystem2 : Subsystem
  tar_sqangle : Outport
  wires:
  Subsystem2/1(tar_sqangle) -> tar_sqangle/1
  now_speed2/1 -> Subsystem2/3(now_speed2)
  now_speed1/1 -> Subsystem2/2(now_speed1)
  tar_speed/1 -> Subsystem2/1(tar_speed)

== system StandTurn_Balance/turnPID ==
  tar_yaw : Inport
  now_yaw : Inport  Port=2
  Enable : EnablePort
  Add : Sum  Inputs=+++  OutDataTypeStr=double
  Add1 : Sum  Inputs=+-
  D : Subsystem
  I : Subsystem
  P : Subsystem
  tar_I : Outport
  wires:
  I/1(Out1) -> Add/2
  tar_yaw/1 -> Add1/1
  now_yaw/1 -> Add1/2
  P/1(Out1) -> Add/1
  Add1/1 -> I/1(error), P/1(error)
  Add/1 -> tar_I/1
  D/1(Out1) -> Add/3

== system StandTurn_Balance/yaw to zero ==
  Enable : EnablePort
  Constant : Constant
  Data Store Read : DataStoreRead  DataStoreName=angle_yaw  IndexOptions=Index vector (dialog)  Indices=1  OutputSizes=1
  Data Store Write : DataStoreWrite  DataStoreName=yaw_begin  IndexOptions=Index vector (dialog)  Indices=1  OutputSizes=1
  Data Store Write1 : DataStoreWrite  DataStoreName=flag  IndexOptions=Index vector (dialog)  Indices=1  OutputSizes=1
  wires:
  Data Store Read/1 -> Data Store Write/1
  Constant/1 -> Data Store Write1/1

== system StandTurn_Balance/zero limit1 ==
  pidout1pwm : Inport
  current1 : Inport  Port=2
  Constant : Constant  Value=10  OutDataTypeStr=int16
  Constant1 : Constant  Value=-10  OutDataTypeStr=int16
  Switch : Switch  Criteria=u2 > Threshold  Threshold=30  OutDataTypeStr=int16
  Switch1 : Switch  Criteria=u2 > Threshold  Threshold=-30  OutDataTypeStr=int16
  Switch2 : Switch  Criteria=u2 > Threshold  OutDataTypeStr=int16
  Switch3 : Switch  Criteria=u2 > Threshold  OutDataTypeStr=int16
  pwmout : Outport
  wires:
  Switch1/1 -> pwmout/1
  Switch2/1 -> Switch/1
  Switch3/1 -> Switch1/3
  Switch/1 -> Switch1/1
  Constant/1 -> Switch2/3
  pidout1pwm/1 -> Switch2/2, Switch3/2, Switch3/3, Switch2/1, Switch/3
  current1/1 -> Switch1/2, Switch/2
  Constant1/1 -> Switch3/1

== system StandTurn_Balance/zero limit2 ==
  pidout2pwm : Inport
  current2 : Inport  Port=2
  Constant : Constant  Value=10  OutDataTypeStr=int16
  Constant1 : Constant  Value=-10  OutDataTypeStr=int16
  Switch : Switch  Criteria=u2 > Threshold  Threshold=30  OutDataTypeStr=int16
  Switch1 : Switch  Criteria=u2 > Threshold  Threshold=-30  OutDataTypeStr=int16
  Switch2 : Switch  Criteria=u2 > Threshold  OutDataTypeStr=int16
  Switch3 : Switch  Criteria=u2 > Threshold  OutDataTypeStr=int16
  pwmout : Outport
  wires:
  Constant1/1 -> Switch3/1
  current2/1 -> Switch/2, Switch1/2
  pidout2pwm/1 -> Switch/3, Switch2/1, Switch3/3, Switch3/2, Switch2/2
  Constant/1 -> Switch2/3
  Switch/1 -> Switch1/1
  Switch3/1 -> Switch1/3
  Switch2/1 -> Switch/1
  Switch1/1 -> pwmout/1

== system StandTurn_Balance/anglePID/D ==
  Constant2 : Constant  Value=0.1
  Data Store Read : DataStoreRead  DataStoreName=angleV_pitch  IndexOptions=Index vector (dialog)  Indices=1  OutputSizes=1
  Data Store Read2 : DataStoreRead  DataStoreName=Kd_angle  IndexOptions=Index vector (dialog)  Indices=1  OutputSizes=1
  Manual Switch2 : ManualSwitch
  Product2 : Product
  Out1 : Outport
  wires:
  Data Store Read/1 -> Product2/2
  Product2/1 -> Out1/1
  Data Store Read2/1 -> Manual Switch2/2
  Manual Switch2/1 -> Product2/1
  Constant2/1 -> Manual Switch2/1

== system StandTurn_Balance/anglePID/P ==
  error : Inport
  Constant : Constant  Value=70
  Data Store Read : DataStoreRead  DataStoreName=Kp_angle  IndexOptions=Index vector (dialog)  Indices=1  OutputSizes=1
  Manual Switch : ManualSwitch
  Product : Product
  Out1 : Outport
  wires:
  error/1 -> Product/2
  Manual Switch/1 -> Product/1
  Data Store Read/1 -> Manual Switch/2
  Constant/1 -> Manual Switch/1
  Product/1 -> Out1/1

== system StandTurn_Balance/currentPID/currentPID_motor1 ==
  tar_current : Inport
  now_current : Inport  Port=2
  Add : Sum  Inputs=+++  OutDataTypeStr=double
  Add1 : Sum  Inputs=+-
  D : Subsystem
  I : Subsystem
  P : Subsystem
  tar_V : Outport
  wires:
  I/1(Out1) -> Add/2
  tar_current/1 -> Add1/1
  now_current/1 -> Add1/2
  P/1(Out1) -> Add/1
  Add1/1 -> D/1(error), I/1(error), P/1(error)
  D/1(Out1) -> Add/3
  Add/1 -> tar_V/1

== system StandTurn_Balance/currentPID/currentPID_motor2 ==
  tar_current : Inport
  now_current : Inport  Port=2
  Add : Sum  Inputs=+++  OutDataTypeStr=double
  Add1 : Sum  Inputs=+-
  D : Subsystem
  I : Subsystem
  P : Subsystem
  tar_V : Outport
  wires:
  Add/1 -> tar_V/1
  D/1(Out1) -> Add/3
  Add1/1 -> P/1(error), I/1(error), D/1(error)
  P/1(Out1) -> Add/1
  now_current/1 -> Add1/2
  tar_current/1 -> Add1/1
  I/1(Out1) -> Add/2

== system StandTurn_Balance/speedPID_motor/Subsystem2 ==
  tar_speed : Inport
  now_speed1 : Inport  Port=2
  now_speed2 : Inport  Port=3
  Add : Sum  Inputs=+++  OutDataTypeStr=double
  Add1 : Sum  Inputs=+-
  Add2 : Sum
  D : Subsystem
  I : Subsystem
  P : Subsystem
  tar_sqangle : Outport
  wires:
  Add2/1 -> Add1/2
  now_speed2/1 -> Add2/2
  now_speed1/1 -> Add2/1
  I/1(Out1) -> Add/2
  Add1/1 -> I/1(error), D/1(error), P/1(error)
  P/1(Out1) -> Add/1
  D/1(Out1) -> Add/3
  Add/1 -> tar_sqangle/1
  tar_speed/1 -> Add1/1

== system StandTurn_Balance/turnPID/D ==
  Constant2 : Constant  Value=0.1
  Data Store Read : DataStoreRead  DataStoreName=angleV_yaw  IndexOptions=Index vector (dialog)  Indices=1  OutputSizes=1
  Data Store Read2 : DataStoreRead  DataStoreName=Kd_turn  IndexOptions=Index vector (dialog)  Indices=1  OutputSizes=1
  Manual Switch2 : ManualSwitch  CurrentSetting=0
  Product2 : Product
  Out1 : Outport
  wires:
  Data Store Read/1 -> Product2/2
  Product2/1 -> Out1/1
  Data Store Read2/1 -> Manual Switch2/2
  Manual Switch2/1 -> Product2/1
  Constant2/1 -> Manual Switch2/1

== system StandTurn_Balance/turnPID/I ==
  error : Inport
  Add2 : Sum
  Constant1 : Constant  Value=0.03
  Data Store Read1 : DataStoreRead  DataStoreName=Ki_turn  IndexOptions=Index vector (dialog)  Indices=1  OutputSizes=1
  Delay : Delay  DelayLength=1
  Gain : Gain  Gain=0.01
  Manual Switch1 : ManualSwitch  CurrentSetting=0
  Product3 : Product  OutDataTypeStr=single
  Saturation : Saturate  UpperLimit=2000  LowerLimit=-2000
  Out1 : Outport
  wires:
  Delay/1 -> Add2/2
  Gain/1 -> Product3/1
  Constant1/1 -> Manual Switch1/1
  Manual Switch1/1 -> Gain/1
  Data Store Read1/1 -> Manual Switch1/2
  Product3/1 -> Add2/1
  error/1 -> Product3/2
  Add2/1 -> Saturation/1
  Saturation/1 -> Delay/1, Out1/1

== system StandTurn_Balance/turnPID/P ==
  error : Inport
  Constant : Constant  Value=-30
  Data Store Read : DataStoreRead  DataStoreName=Kp_turn  IndexOptions=Index vector (dialog)  Indices=1  OutputSizes=1
  Manual Switch : ManualSwitch  CurrentSetting=0
  Product : Product
  Out1 : Outport
  wires:
  error/1 -> Product/2
  Manual Switch/1 -> Product/1
  Data Store Read/1 -> Manual Switch/2
  Constant/1 -> Manual Switch/1
  Product/1 -> Out1/1

== system StandTurn_Balance/currentPID/currentPID_motor1/D ==
  error : Inport
  Constant2 : Constant  Value=5
  Data Store Read2 : DataStoreRead  DataStoreName=Kd_current  IndexOptions=Index vector (dialog)  Indices=1  OutputSizes=1
  Difference : simulink/Discrete/Difference  ICPrevInput=0.0  OutMin=[]  OutMax=[]  OutDataType=fixdt(1, 16)  OutScaling=2^-10  DoSatur=off
  Manual Switch2 : ManualSwitch
  Product2 : Product
  Out1 : Outport
  wires:
  Difference/1 -> Product2/2
  Product2/1 -> Out1/1
  Data Store Read2/1 -> Manual Switch2/2
  Manual Switch2/1 -> Product2/1
  Constant2/1 -> Manual Switch2/1
  error/1 -> Difference/1

== system StandTurn_Balance/currentPID/currentPID_motor1/I ==
  error : Inport
  Add2 : Sum
  Constant1 : Constant  Value=3
  Data Store Read1 : DataStoreRead  DataStoreName=Ki_current  IndexOptions=Index vector (dialog)  Indices=1  OutputSizes=1
  Delay : Delay  DelayLength=1
  Gain : Gain  Gain=0.01
  Manual Switch1 : ManualSwitch
  Product3 : Product  OutDataTypeStr=single
  Saturation : Saturate  UpperLimit=2000  LowerLimit=-2000
  Out1 : Outport
  wires:
  Delay/1 -> Add2/2
  Gain/1 -> Product3/1
  Constant1/1 -> Manual Switch1/1
  Manual Switch1/1 -> Gain/1
  Data Store Read1/1 -> Manual Switch1/2
  Product3/1 -> Add2/1
  error/1 -> Product3/2
  Add2/1 -> Saturation/1
  Saturation/1 -> Delay/1, Out1/1

== system StandTurn_Balance/currentPID/currentPID_motor1/P ==
  error : Inport
  Constant : Constant  Value=7
  Data Store Read : DataStoreRead  DataStoreName=Kp_current  IndexOptions=Index vector (dialog)  Indices=1  OutputSizes=1
  Manual Switch : ManualSwitch
  Product : Product
  Out1 : Outport
  wires:
  error/1 -> Product/2
  Manual Switch/1 -> Product/1
  Data Store Read/1 -> Manual Switch/2
  Constant/1 -> Manual Switch/1
  Product/1 -> Out1/1

== system StandTurn_Balance/currentPID/currentPID_motor2/D ==
  error : Inport
  Constant2 : Constant  Value=4
  Data Store Read2 : DataStoreRead  DataStoreName=Kd_current  IndexOptions=Index vector (dialog)  Indices=1  OutputSizes=1
  Difference : simulink/Discrete/Difference  ICPrevInput=0.0  OutMin=[]  OutMax=[]  OutDataType=fixdt(1, 16)  OutScaling=2^-10  DoSatur=off
  Manual Switch2 : ManualSwitch
  Product2 : Product
  Out1 : Outport
  wires:
  error/1 -> Difference/1
  Constant2/1 -> Manual Switch2/1
  Manual Switch2/1 -> Product2/1
  Data Store Read2/1 -> Manual Switch2/2
  Product2/1 -> Out1/1
  Difference/1 -> Product2/2

== system StandTurn_Balance/currentPID/currentPID_motor2/I ==
  error : Inport
  Add2 : Sum
  Constant1 : Constant  Value=3
  Data Store Read1 : DataStoreRead  DataStoreName=Ki_current  IndexOptions=Index vector (dialog)  Indices=1  OutputSizes=1
  Delay : Delay  DelayLength=1
  Gain : Gain  Gain=0.01
  Manual Switch1 : ManualSwitch
  Product3 : Product  OutDataTypeStr=single
  Saturation : Saturate  UpperLimit=2000  LowerLimit=-2000
  Out1 : Outport
  wires:
  Add2/1 -> Saturation/1
  error/1 -> Product3/2
  Product3/1 -> Add2/1
  Data Store Read1/1 -> Manual Switch1/2
  Manual Switch1/1 -> Gain/1
  Constant1/1 -> Manual Switch1/1
  Gain/1 -> Product3/1
  Delay/1 -> Add2/2
  Saturation/1 -> Out1/1, Delay/1

== system StandTurn_Balance/currentPID/currentPID_motor2/P ==
  error : Inport
  Constant : Constant  Value=7
  Data Store Read : DataStoreRead  DataStoreName=Kp_current  IndexOptions=Index vector (dialog)  Indices=1  OutputSizes=1
  Manual Switch : ManualSwitch
  Product : Product
  Out1 : Outport
  wires:
  Product/1 -> Out1/1
  Constant/1 -> Manual Switch/1
  Data Store Read/1 -> Manual Switch/2
  Manual Switch/1 -> Product/1
  error/1 -> Product/2

== system StandTurn_Balance/speedPID_motor/Subsystem2/D ==
  error : Inport
  Constant2 : Constant  Value=-100
  Data Store Read2 : DataStoreRead  DataStoreName=Kd_speed  IndexOptions=Index vector (dialog)  Indices=1  OutputSizes=1
  Difference : simulink/Discrete/Difference  ICPrevInput=0.0  OutMin=[]  OutMax=[]  OutDataType=fixdt(1, 16)  OutScaling=2^-10  DoSatur=off
  Gain : Gain  Gain=0.001
  Manual Switch2 : ManualSwitch  CurrentSetting=0
  Product2 : Product
  Out1 : Outport
  wires:
  Difference/1 -> Product2/2
  Product2/1 -> Out1/1
  Data Store Read2/1 -> Manual Switch2/2
  Manual Switch2/1 -> Gain/1
  Constant2/1 -> Manual Switch2/1
  error/1 -> Difference/1
  Gain/1 -> Product2/1

== system StandTurn_Balance/speedPID_motor/Subsystem2/I ==
  error : Inport
  Add2 : Sum
  Constant1 : Constant  Value=-14
  Data Store Read1 : DataStoreRead  DataStoreName=Ki_speed  IndexOptions=Index vector (dialog)  Indices=1  OutputSizes=1
  Delay : Delay  DelayLength=1
  Gain : Gain  Gain=0.001
  Gain1 : Gain  Gain=0.995
  Manual Switch1 : ManualSwitch  CurrentSetting=0
  Product3 : Product  OutDataTypeStr=single
  Saturation2 : Saturate  UpperLimit=1500  LowerLimit=-1500
  Out1 : Outport
  wires:
  Delay/1 -> Add2/2
  Gain/1 -> Product3/1
  Add2/1 -> Gain1/1
  Constant1/1 -> Manual Switch1/1
  Manual Switch1/1 -> Gain/1
  Data Store Read1/1 -> Manual Switch1/2
  Gain1/1 -> Saturation2/1
  Product3/1 -> Add2/1
  error/1 -> Product3/2
  Saturation2/1 -> Out1/1, Delay/1

== system StandTurn_Balance/speedPID_motor/Subsystem2/P ==
  error : Inport
  Constant : Constant  Value=-4
  Data Store Read : DataStoreRead  DataStoreName=Kp_speed  IndexOptions=Index vector (dialog)  Indices=1  OutputSizes=1
  Gain : Gain  Gain=0.001
  Manual Switch : ManualSwitch  CurrentSetting=0
  Product : Product
  Out1 : Outport
  wires:
  error/1 -> Product/2
  Data Store Read/1 -> Manual Switch/2
  Constant/1 -> Manual Switch/1
  Product/1 -> Out1/1
  Manual Switch/1 -> Gain/1
  Gain/1 -> Product/1
